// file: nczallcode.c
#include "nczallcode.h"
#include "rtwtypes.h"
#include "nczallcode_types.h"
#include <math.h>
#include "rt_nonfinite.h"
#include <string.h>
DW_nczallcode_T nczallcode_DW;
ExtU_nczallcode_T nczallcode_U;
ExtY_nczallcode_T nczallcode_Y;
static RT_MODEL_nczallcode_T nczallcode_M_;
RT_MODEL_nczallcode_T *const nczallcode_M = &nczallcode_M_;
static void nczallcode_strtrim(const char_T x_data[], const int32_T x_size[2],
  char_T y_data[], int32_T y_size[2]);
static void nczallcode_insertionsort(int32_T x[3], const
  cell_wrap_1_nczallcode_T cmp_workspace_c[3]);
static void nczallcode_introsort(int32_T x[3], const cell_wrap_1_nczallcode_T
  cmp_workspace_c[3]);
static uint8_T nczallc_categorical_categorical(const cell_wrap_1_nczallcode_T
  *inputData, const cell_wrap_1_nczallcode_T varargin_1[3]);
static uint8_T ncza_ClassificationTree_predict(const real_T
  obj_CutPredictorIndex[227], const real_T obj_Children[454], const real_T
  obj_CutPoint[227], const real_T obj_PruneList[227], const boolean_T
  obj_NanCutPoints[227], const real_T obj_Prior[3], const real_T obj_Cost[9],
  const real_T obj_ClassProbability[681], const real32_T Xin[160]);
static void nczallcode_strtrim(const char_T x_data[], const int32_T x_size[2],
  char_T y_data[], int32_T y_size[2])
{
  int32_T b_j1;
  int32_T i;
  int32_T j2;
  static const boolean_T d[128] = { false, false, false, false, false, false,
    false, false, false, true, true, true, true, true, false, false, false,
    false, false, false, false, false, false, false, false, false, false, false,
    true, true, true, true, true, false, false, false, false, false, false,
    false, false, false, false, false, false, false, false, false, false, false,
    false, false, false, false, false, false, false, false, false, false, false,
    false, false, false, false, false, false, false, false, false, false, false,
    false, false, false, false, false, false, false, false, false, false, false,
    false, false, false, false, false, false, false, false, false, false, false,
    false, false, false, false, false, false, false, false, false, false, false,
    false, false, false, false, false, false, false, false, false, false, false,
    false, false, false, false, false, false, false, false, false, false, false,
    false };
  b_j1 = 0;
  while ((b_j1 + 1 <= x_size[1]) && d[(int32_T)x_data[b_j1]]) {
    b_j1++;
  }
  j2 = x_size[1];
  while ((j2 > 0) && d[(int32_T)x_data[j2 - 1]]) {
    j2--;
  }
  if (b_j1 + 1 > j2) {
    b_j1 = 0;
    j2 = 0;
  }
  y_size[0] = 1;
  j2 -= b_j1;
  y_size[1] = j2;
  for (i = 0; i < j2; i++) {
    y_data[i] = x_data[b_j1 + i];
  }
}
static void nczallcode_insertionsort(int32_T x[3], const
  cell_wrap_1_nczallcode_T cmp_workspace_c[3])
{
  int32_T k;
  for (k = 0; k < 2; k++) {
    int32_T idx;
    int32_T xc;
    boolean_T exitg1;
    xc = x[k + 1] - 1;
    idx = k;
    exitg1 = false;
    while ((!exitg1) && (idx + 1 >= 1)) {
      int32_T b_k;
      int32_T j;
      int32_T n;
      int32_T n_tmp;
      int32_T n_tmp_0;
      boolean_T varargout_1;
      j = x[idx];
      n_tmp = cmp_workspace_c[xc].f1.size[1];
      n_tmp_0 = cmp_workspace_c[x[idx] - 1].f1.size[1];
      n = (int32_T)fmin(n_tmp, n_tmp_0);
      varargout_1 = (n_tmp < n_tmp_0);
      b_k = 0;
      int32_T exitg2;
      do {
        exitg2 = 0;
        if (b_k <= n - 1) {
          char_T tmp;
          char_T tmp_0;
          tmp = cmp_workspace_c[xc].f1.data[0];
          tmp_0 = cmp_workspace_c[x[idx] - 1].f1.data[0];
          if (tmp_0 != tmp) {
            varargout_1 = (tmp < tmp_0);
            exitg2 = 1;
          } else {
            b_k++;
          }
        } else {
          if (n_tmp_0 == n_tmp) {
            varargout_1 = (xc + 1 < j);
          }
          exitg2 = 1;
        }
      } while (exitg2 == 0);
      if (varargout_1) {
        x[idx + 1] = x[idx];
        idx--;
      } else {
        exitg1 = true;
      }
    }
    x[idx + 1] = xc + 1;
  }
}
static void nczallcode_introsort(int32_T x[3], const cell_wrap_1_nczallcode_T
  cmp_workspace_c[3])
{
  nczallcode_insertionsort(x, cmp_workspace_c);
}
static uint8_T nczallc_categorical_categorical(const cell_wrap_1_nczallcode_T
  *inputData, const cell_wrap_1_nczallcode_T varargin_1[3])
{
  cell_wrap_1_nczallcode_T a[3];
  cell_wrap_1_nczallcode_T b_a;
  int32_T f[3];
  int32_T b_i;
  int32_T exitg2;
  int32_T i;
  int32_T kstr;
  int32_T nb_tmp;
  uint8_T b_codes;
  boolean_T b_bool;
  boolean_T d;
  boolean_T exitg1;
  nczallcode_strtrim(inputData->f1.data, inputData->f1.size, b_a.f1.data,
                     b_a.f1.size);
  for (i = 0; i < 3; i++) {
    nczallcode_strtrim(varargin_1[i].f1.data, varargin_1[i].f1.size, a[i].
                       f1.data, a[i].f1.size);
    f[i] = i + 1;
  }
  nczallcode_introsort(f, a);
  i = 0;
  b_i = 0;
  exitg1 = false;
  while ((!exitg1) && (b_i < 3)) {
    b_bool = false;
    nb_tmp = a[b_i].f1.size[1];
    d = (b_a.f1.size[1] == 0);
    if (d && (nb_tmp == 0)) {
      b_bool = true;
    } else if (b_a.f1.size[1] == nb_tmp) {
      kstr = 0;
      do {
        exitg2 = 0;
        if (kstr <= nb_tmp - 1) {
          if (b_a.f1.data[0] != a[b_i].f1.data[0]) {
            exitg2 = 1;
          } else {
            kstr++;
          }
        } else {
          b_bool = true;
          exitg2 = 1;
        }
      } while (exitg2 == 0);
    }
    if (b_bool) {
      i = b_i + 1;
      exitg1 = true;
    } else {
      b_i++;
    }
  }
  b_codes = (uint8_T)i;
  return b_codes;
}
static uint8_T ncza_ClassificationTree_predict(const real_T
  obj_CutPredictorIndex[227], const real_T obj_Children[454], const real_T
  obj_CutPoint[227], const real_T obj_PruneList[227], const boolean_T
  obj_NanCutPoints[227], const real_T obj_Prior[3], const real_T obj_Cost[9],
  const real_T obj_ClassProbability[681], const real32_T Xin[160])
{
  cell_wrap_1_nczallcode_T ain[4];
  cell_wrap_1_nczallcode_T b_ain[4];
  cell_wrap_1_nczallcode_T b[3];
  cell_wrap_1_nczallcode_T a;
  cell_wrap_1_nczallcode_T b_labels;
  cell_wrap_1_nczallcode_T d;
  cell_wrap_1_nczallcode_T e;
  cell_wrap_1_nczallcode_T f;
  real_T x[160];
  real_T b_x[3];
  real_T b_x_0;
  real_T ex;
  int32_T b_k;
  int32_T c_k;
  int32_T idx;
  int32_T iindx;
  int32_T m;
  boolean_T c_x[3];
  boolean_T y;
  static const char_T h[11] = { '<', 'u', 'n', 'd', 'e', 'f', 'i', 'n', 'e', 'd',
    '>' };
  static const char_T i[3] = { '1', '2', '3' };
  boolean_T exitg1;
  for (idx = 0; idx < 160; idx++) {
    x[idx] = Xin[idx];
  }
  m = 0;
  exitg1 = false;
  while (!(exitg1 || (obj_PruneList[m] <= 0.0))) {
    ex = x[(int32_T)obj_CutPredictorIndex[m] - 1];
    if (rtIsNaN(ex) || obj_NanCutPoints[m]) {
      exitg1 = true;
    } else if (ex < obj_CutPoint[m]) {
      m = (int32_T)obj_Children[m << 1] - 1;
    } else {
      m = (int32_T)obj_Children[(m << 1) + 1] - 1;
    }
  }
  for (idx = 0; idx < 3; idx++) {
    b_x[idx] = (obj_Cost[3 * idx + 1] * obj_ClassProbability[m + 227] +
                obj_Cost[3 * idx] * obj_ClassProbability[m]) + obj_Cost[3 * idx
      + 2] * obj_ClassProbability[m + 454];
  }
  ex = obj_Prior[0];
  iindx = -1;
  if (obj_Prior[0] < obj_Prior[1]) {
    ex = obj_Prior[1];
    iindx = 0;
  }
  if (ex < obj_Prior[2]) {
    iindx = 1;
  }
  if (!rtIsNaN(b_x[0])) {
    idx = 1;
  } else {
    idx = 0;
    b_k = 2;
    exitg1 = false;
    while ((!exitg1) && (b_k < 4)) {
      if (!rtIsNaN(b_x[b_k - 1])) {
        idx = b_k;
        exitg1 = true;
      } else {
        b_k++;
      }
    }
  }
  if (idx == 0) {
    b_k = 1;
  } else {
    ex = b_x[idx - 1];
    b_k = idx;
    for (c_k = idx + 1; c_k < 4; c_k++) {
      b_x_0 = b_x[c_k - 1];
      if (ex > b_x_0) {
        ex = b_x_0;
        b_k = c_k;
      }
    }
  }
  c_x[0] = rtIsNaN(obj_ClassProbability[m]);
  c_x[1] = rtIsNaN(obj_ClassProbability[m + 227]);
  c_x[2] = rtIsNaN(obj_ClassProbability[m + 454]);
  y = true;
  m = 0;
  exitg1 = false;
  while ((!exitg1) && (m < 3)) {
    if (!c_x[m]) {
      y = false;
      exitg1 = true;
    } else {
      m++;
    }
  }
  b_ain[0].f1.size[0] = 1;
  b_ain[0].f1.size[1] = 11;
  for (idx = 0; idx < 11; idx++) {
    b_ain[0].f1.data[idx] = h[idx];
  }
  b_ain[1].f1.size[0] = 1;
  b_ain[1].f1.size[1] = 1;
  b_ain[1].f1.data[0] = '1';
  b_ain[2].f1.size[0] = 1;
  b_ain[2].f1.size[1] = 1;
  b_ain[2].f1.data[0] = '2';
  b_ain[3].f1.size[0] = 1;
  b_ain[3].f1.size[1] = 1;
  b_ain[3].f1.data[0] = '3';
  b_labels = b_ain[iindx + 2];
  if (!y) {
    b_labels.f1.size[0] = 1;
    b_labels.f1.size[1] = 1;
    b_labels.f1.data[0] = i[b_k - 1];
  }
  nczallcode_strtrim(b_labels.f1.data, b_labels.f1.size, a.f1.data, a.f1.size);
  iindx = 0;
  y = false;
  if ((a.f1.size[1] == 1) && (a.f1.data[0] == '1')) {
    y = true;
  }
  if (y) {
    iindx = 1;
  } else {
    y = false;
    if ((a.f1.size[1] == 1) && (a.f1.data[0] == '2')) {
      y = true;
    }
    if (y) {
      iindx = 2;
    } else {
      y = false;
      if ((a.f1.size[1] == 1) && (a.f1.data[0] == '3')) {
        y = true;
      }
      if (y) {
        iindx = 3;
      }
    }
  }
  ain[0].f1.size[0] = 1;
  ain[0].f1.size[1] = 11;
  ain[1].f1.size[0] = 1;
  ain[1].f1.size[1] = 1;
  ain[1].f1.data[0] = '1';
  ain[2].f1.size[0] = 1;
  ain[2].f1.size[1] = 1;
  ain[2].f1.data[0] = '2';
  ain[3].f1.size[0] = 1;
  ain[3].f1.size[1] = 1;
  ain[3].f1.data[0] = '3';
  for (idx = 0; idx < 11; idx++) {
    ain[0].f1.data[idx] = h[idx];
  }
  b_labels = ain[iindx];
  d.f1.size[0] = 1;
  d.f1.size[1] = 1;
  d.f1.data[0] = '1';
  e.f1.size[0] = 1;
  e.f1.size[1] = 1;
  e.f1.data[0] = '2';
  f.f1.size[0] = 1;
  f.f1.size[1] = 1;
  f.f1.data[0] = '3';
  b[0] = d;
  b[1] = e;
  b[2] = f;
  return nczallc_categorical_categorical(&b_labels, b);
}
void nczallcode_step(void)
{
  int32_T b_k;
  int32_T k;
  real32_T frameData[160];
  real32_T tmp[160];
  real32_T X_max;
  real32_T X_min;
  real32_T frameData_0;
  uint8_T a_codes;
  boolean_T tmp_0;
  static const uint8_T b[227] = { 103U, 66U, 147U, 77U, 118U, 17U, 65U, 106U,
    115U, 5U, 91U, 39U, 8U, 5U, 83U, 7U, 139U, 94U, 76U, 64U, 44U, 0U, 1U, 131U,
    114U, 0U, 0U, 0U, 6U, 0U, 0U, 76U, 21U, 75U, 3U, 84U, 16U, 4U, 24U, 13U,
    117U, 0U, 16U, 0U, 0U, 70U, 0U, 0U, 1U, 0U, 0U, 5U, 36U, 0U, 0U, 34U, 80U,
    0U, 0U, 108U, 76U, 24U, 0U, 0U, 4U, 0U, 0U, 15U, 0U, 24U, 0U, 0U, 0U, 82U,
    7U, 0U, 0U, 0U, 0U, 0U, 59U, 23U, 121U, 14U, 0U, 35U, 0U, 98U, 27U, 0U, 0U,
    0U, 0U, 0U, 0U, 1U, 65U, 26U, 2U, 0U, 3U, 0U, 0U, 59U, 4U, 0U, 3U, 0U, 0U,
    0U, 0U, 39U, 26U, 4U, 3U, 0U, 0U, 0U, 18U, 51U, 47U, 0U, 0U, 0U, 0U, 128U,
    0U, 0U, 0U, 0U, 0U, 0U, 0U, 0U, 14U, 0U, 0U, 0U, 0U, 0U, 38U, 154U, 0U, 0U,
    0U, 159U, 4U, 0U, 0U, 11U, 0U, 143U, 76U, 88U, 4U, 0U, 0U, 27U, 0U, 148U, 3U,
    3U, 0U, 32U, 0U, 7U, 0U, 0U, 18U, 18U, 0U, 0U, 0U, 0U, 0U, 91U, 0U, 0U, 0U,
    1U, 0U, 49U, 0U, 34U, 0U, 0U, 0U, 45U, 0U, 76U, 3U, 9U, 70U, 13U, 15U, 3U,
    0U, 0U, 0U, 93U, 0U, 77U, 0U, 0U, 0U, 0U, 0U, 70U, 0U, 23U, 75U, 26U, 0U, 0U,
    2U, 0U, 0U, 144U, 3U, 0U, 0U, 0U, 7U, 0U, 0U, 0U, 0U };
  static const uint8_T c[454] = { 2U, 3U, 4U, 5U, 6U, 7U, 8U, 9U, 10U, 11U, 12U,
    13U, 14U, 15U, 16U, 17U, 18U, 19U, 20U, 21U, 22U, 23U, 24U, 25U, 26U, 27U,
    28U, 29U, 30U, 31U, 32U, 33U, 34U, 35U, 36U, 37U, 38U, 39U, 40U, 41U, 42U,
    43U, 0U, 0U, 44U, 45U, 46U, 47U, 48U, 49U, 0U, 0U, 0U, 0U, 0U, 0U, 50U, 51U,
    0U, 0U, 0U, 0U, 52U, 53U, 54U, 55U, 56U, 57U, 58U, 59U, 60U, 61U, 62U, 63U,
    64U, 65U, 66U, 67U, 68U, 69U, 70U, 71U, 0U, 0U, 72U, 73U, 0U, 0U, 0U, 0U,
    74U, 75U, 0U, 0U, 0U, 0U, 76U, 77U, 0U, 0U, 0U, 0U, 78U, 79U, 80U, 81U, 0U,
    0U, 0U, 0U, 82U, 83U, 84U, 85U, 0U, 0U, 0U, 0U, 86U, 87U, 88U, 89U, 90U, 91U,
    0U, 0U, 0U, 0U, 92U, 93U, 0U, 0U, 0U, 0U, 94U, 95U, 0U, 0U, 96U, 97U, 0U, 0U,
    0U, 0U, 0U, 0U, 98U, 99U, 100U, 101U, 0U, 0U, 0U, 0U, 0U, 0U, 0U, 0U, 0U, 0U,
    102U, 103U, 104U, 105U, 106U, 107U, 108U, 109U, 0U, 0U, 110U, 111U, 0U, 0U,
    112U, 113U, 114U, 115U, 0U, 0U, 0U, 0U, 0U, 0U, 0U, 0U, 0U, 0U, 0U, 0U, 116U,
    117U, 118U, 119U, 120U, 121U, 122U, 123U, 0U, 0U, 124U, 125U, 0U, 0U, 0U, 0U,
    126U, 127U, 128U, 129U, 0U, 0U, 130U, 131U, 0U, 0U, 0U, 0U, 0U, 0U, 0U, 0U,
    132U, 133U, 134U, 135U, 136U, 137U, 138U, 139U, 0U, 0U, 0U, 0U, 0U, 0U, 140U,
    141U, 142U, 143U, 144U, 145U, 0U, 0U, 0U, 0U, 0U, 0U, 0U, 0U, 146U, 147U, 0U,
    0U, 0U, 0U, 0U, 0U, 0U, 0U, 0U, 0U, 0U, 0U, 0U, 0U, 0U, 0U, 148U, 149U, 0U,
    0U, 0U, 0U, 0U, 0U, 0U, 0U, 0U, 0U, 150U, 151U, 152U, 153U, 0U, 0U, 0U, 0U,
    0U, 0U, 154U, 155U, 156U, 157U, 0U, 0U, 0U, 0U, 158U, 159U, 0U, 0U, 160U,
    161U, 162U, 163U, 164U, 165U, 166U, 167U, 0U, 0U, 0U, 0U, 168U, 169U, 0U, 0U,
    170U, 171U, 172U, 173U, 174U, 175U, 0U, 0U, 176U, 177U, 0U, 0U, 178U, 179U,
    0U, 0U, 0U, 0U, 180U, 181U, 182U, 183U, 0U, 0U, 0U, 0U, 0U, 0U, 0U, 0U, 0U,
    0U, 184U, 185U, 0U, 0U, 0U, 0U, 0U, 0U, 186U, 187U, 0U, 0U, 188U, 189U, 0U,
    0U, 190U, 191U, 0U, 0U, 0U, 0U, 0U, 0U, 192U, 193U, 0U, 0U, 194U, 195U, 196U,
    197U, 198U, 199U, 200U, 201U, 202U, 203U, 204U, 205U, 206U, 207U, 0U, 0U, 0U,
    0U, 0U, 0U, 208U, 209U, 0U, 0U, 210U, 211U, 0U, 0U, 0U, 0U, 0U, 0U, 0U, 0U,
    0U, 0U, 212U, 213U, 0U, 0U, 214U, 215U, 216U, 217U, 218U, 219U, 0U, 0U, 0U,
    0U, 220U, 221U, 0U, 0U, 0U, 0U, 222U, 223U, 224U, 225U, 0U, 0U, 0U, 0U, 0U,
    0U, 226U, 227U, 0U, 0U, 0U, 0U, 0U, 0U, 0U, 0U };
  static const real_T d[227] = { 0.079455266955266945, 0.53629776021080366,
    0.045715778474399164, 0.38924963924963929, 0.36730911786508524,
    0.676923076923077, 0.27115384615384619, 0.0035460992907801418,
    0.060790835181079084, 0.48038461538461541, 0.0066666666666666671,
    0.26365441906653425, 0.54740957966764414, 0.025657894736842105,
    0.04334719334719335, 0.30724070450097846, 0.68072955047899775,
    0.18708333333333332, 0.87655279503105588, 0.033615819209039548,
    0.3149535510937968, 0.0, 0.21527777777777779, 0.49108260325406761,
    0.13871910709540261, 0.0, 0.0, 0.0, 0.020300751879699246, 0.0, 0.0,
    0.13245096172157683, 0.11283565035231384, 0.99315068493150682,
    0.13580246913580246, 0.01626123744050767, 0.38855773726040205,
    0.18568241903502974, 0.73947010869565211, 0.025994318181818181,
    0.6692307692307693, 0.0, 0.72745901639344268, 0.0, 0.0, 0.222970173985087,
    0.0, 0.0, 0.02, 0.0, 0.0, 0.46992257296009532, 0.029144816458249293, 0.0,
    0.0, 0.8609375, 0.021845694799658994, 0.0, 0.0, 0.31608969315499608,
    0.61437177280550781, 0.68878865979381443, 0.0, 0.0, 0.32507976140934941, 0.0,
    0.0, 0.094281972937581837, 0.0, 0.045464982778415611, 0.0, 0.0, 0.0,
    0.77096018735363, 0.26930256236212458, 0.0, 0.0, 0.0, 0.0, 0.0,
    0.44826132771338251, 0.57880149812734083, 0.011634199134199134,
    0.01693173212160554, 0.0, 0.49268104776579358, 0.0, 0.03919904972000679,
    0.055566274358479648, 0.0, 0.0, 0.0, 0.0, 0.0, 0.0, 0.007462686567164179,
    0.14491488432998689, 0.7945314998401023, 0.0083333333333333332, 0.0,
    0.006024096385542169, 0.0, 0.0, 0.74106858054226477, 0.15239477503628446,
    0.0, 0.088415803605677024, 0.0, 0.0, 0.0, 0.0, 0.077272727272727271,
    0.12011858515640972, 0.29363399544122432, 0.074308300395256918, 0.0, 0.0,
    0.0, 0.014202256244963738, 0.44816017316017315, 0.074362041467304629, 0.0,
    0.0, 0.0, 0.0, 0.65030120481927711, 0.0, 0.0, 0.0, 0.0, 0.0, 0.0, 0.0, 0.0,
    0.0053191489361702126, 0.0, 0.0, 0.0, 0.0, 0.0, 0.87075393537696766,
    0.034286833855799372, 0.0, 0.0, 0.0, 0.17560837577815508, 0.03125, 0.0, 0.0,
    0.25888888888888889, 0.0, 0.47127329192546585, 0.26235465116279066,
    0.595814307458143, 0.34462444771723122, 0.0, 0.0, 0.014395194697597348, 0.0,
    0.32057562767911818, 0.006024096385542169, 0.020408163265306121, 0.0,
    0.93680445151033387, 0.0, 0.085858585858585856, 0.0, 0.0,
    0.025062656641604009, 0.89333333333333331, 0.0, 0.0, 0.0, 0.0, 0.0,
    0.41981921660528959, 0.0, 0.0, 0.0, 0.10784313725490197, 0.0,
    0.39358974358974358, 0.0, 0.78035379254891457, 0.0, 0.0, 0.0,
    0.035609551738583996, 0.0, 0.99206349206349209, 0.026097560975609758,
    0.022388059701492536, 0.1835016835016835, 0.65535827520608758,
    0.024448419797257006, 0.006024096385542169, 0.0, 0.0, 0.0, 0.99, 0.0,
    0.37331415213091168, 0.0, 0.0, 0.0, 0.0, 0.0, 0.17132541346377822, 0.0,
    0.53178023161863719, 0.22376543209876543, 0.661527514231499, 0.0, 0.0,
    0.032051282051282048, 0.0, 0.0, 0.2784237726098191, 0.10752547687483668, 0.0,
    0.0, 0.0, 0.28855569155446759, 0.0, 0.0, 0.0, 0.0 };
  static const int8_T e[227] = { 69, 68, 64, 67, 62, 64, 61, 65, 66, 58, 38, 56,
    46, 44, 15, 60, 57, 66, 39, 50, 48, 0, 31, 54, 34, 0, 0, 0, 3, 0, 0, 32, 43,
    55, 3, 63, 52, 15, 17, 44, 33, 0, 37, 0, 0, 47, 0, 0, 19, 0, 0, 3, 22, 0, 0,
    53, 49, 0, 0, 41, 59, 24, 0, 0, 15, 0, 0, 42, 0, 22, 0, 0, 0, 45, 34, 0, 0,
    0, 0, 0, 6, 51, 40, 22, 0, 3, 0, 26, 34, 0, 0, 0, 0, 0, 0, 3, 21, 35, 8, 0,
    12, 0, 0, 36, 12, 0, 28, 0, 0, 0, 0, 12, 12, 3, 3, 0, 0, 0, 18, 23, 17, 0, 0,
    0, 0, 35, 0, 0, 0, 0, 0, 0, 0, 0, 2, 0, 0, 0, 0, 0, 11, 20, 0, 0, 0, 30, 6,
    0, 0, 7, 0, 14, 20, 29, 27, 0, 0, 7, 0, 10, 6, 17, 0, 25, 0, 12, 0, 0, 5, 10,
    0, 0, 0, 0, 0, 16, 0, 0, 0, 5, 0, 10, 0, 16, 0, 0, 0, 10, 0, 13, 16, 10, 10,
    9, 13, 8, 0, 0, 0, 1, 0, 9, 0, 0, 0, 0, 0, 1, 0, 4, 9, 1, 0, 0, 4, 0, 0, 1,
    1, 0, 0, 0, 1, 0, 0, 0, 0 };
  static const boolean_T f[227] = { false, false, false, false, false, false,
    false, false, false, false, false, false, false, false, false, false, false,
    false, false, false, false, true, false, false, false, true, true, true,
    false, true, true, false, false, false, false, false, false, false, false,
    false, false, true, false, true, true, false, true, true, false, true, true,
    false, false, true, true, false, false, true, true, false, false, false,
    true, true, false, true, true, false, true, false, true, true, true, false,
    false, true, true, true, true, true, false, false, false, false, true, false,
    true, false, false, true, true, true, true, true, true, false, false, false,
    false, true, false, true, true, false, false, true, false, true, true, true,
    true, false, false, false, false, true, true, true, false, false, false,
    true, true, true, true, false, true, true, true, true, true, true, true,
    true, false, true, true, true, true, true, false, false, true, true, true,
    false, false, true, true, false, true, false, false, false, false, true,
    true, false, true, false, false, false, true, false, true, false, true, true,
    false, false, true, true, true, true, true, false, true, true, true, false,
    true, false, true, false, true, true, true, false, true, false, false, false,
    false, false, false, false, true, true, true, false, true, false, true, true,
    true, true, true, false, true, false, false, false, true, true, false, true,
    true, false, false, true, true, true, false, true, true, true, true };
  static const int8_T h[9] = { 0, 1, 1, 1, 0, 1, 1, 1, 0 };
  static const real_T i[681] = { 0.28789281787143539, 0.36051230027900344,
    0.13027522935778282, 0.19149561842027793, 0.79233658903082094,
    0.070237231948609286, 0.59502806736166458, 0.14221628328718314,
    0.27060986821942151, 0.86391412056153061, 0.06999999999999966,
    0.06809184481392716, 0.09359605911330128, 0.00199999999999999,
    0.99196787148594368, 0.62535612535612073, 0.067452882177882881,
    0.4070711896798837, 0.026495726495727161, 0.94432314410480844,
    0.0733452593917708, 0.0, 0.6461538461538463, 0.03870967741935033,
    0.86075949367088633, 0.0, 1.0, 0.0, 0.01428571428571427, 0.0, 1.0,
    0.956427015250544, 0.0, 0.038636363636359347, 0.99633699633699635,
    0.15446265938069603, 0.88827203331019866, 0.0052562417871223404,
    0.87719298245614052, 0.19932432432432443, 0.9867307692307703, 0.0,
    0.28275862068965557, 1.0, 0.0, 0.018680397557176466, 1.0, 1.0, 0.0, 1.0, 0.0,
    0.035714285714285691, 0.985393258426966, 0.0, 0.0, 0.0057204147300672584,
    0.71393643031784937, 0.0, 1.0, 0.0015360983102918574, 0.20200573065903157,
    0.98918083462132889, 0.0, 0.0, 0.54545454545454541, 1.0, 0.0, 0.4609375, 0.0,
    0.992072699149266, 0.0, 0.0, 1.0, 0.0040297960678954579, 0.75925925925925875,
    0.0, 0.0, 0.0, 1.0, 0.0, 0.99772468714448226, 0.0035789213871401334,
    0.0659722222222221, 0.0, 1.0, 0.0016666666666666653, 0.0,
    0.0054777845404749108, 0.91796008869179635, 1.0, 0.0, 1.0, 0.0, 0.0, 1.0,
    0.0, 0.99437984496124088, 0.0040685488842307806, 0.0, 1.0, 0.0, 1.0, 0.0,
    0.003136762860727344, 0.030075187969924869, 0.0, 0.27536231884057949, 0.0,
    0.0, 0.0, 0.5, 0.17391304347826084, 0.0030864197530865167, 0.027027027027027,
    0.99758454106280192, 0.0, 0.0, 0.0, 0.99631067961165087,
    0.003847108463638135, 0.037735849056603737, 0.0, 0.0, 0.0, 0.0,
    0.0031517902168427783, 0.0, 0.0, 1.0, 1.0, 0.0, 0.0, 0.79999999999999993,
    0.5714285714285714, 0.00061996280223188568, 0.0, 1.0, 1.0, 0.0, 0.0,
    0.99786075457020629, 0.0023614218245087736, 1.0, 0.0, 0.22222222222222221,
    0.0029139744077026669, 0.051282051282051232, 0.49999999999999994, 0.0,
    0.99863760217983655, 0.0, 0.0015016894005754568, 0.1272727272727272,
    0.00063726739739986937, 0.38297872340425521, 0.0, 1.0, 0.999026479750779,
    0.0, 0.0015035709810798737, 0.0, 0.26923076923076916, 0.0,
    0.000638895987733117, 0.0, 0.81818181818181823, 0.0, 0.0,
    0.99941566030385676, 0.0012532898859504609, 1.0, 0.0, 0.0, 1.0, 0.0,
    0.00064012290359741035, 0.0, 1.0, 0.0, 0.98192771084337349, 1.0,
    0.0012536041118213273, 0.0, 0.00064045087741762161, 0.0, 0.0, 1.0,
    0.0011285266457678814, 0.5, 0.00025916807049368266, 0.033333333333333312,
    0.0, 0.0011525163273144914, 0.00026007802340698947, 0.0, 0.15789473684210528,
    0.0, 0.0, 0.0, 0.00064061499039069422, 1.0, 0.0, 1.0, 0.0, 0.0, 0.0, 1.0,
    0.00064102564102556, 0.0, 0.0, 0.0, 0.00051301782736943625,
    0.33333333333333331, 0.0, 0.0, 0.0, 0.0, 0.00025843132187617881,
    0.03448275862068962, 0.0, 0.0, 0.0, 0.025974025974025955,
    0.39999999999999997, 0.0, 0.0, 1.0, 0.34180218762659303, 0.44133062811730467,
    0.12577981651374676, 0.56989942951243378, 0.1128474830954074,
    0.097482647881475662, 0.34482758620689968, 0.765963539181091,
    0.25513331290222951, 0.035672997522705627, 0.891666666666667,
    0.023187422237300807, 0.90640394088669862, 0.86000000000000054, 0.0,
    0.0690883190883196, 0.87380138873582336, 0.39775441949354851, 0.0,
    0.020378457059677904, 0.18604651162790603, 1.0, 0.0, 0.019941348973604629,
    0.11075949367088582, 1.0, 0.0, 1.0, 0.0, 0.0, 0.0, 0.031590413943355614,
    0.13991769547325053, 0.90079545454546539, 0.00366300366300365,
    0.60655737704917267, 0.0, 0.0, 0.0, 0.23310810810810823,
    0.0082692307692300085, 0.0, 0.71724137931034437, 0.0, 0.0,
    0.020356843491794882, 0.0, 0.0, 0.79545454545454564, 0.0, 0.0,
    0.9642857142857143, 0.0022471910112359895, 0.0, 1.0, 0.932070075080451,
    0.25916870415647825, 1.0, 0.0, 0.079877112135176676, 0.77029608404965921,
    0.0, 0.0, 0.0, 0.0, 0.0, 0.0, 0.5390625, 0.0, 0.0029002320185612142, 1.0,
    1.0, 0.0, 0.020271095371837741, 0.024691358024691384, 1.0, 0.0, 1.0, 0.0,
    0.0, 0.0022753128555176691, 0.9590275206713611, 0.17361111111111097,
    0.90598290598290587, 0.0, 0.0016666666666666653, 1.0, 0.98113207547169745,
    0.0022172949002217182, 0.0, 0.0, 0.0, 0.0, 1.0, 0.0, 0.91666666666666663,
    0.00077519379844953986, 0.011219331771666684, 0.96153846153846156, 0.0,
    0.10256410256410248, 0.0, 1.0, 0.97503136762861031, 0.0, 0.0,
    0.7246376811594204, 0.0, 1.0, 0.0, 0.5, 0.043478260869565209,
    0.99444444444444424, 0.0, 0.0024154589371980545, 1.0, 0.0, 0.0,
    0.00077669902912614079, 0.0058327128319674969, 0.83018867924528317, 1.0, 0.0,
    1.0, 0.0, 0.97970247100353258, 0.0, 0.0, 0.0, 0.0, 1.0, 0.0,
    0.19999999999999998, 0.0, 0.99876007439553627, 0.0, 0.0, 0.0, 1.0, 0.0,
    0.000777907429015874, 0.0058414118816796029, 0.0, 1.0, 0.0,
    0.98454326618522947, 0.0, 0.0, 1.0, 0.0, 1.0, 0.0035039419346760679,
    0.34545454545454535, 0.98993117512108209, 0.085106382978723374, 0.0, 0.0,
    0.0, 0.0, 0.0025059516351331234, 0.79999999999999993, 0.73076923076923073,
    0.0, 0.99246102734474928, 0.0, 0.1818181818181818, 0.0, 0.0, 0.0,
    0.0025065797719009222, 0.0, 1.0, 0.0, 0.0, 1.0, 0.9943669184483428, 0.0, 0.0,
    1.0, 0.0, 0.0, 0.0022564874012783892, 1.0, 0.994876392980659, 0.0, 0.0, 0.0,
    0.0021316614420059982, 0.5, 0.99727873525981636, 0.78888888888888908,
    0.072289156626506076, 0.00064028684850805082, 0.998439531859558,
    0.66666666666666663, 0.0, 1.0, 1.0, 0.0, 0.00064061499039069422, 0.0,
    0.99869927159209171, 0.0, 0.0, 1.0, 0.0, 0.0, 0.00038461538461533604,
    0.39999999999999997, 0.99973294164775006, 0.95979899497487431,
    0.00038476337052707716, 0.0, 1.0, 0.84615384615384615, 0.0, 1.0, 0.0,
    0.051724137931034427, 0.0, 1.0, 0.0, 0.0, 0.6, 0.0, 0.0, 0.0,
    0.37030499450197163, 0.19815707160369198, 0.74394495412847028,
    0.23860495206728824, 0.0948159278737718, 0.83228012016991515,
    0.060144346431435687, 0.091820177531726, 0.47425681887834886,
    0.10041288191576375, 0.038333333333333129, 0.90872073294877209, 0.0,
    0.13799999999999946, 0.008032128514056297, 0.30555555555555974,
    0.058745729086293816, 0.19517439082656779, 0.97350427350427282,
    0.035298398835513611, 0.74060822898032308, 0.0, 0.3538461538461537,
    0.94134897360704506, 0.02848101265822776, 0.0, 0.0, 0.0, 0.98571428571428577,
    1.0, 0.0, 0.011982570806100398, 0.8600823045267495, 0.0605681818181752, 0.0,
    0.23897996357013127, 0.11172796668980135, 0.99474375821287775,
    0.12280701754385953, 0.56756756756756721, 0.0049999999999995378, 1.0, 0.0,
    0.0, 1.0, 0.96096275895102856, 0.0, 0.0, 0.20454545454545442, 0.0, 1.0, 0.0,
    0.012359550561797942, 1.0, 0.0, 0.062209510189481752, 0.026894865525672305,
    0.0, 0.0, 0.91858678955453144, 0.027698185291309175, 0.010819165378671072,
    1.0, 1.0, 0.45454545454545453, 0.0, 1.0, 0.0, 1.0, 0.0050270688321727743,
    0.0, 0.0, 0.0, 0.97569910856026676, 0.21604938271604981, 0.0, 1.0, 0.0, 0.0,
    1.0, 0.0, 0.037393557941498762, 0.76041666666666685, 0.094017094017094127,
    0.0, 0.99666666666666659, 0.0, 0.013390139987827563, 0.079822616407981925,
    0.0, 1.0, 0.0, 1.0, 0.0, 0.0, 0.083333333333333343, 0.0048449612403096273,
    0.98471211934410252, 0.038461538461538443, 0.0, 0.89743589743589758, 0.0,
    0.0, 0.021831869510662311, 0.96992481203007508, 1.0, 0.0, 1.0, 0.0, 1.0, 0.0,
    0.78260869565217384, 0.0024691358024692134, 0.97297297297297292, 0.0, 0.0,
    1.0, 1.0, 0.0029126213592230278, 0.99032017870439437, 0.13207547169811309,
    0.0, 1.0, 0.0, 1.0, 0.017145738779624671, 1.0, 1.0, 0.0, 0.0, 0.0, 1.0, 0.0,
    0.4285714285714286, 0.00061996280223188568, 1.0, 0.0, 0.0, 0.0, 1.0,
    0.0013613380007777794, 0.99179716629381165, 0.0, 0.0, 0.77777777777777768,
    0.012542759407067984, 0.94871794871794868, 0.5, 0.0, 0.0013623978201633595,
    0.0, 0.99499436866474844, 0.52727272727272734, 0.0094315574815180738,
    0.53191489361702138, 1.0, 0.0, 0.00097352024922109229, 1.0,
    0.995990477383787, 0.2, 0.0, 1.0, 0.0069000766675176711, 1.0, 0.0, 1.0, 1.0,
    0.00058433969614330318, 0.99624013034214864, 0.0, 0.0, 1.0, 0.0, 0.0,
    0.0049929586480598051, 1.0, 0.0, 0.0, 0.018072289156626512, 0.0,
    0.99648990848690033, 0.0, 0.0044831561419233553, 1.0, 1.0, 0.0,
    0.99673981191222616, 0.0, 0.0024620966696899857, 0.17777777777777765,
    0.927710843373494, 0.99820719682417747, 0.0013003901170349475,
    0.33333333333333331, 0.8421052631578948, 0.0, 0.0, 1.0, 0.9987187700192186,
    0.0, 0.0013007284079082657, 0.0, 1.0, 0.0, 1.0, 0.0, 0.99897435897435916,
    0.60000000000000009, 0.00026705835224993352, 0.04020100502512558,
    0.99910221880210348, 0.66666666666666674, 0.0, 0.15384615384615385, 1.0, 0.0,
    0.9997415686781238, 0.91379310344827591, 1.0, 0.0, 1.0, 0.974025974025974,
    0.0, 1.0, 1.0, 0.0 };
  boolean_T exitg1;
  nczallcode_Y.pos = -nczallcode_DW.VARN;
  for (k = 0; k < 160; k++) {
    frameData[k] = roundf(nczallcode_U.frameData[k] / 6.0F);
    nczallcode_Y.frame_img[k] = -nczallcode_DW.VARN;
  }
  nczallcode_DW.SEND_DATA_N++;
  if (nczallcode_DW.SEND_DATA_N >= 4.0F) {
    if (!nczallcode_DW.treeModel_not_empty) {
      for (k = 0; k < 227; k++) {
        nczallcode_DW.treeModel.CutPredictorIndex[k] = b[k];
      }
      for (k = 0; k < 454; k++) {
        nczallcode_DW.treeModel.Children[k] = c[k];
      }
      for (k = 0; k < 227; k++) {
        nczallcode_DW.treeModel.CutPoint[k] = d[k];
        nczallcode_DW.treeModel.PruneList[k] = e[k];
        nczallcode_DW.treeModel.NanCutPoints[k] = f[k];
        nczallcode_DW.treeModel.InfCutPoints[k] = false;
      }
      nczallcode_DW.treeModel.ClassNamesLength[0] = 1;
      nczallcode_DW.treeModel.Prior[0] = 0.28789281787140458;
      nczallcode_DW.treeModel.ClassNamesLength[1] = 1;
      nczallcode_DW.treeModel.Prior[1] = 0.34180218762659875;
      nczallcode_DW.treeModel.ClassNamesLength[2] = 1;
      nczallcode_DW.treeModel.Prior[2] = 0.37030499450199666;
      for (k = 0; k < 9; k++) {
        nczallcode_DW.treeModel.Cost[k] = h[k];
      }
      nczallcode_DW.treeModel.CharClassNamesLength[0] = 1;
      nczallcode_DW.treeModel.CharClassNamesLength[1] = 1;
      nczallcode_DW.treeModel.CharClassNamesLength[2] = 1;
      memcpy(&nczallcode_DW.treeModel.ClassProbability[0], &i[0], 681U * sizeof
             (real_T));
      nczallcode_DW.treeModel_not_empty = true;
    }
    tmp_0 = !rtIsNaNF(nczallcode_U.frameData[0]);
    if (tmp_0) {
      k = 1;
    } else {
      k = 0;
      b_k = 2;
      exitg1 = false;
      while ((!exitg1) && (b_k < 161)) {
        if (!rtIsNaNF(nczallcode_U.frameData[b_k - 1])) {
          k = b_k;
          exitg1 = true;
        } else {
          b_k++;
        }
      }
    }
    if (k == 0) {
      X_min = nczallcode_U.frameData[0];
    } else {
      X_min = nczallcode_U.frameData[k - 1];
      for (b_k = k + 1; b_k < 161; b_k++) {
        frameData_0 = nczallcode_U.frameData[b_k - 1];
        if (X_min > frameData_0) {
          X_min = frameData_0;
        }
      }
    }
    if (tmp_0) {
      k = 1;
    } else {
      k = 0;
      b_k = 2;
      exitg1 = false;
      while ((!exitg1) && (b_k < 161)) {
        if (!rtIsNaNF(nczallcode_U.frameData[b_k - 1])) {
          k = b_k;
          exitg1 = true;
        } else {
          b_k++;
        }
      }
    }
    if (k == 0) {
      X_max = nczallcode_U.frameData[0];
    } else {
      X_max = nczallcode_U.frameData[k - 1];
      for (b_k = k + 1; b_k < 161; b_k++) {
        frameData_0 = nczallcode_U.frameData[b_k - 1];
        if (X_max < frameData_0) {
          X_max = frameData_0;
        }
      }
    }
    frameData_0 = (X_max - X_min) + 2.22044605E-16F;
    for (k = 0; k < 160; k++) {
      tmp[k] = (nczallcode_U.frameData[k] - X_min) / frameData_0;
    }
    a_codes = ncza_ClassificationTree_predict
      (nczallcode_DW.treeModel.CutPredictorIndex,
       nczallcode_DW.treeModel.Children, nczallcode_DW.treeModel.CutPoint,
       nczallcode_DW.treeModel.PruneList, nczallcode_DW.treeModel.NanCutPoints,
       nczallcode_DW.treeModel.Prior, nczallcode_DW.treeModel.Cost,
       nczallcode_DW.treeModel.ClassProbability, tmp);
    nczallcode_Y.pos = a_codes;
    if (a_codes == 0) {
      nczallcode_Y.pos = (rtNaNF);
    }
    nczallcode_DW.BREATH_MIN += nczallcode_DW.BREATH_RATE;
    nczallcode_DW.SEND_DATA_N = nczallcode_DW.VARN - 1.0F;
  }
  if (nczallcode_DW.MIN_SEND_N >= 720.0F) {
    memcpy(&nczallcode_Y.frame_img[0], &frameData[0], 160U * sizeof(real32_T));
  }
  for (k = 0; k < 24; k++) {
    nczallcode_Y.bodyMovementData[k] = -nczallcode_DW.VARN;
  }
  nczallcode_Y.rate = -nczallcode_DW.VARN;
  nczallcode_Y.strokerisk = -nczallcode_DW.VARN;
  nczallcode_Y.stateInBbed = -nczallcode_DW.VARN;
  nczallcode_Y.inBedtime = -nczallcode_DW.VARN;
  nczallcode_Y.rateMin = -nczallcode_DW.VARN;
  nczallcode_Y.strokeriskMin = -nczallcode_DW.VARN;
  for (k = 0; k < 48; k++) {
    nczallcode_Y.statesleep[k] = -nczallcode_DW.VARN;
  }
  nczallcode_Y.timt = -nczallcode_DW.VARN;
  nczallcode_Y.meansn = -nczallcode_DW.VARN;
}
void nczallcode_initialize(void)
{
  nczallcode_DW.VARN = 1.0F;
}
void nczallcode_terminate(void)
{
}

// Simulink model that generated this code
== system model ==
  frameData : Inport
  Inport#1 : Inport
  bodyMovementData : Outport  <- 1: MATLABFunction#1
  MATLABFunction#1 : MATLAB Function  <- 1: frameData, 2: Inport#1
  rate : Outport  <- 1: MATLABFunction#1/2
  strokerisk : Outport  <- 1: MATLABFunction#1/3
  stateInBbed : Outport  <- 1: MATLABFunction#1/4
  inBedtime : Outport  <- 1: MATLABFunction#1/5
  rateMin : Outport  <- 1: MATLABFunction#1/6
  strokeriskMin : Outport  <- 1: MATLABFunction#1/7
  statesleep : Outport  <- 1: MATLABFunction#1/8
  timt : Outport  <- 1: MATLABFunction#1/9
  meansn : Outport  <- 1: MATLABFunction#1/10
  frame_img : Outport  <- 1: MATLABFunction#1/11
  pos : Outport  <- 1: MATLABFunction#1/12
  DataStoreMemory#1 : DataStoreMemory  DataStoreName=VARN  InitialValue=1
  DataStoreMemory#2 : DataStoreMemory  DataStoreName=G_INBED_TIM
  DataStoreMemory#3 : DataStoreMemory  DataStoreName=Awake_sleep_array  InitialValue=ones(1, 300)
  DataStoreMemory#4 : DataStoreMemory  DataStoreName=BREATH_RATE
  DataStoreMemory#5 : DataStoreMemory  DataStoreName=MIN_SEND_N
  DataStoreMemory#6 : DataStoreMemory  DataStoreName=STROKE_RISK_MIN
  DataStoreMemory#7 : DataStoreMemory  DataStoreName=BREATH_MIN
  DataStoreMemory#8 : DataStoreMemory  DataStoreName=BATCH_FRA_MEAN
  DataStoreMemory#9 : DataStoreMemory  DataStoreName=TWENTY_SEC
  DataStoreMemory#10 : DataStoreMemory  DataStoreName=STATE_SLEEP  InitialValue=[0,0,0,0,0,0,0,0,0,0,0,0,0,0,0,0,0,0,0,0,0,0,0,0,0,0,0,0,0,0,0,0,0,0,0,0,0,0,0,0,0,0,0,0,0,0,0,0]
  DataStoreMemory#11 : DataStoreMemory  DataStoreName=FRAME_DIFF  InitialValue=[0,0,0,0,0,0,0,0,0,0,0,0,0,0,0,0]
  DataStoreMemory#12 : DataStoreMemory  DataStoreName=ITER
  DataStoreMemory#13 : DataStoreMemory  DataStoreName=G_STATE_INBED
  DataStoreMemory#14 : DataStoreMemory  DataStoreName=L_R_M_FREATUE  InitialValue=[0,0,0,0,0,0,0,0,0,0,0,0,0,0,0,0,0,0,0,0,0,0,0,0,0,0,0,0,0,0,0,0,0,0,0,0,0,0,0,0,0,0,0,0,0,0,0,0,0,0,0,0,0,0,0,0,0,0,0,0,0,0,0,0,0,0,0,0,0,0,0,0,0,0,0,0,0,0,0,0,0,0,0,0,0,0,0,0,0,0,0,0,0,0,0,0,0,0,0,0,0,0,0,0,0,0,0,0,0,0,0,0,0,0,0,0,0,0,0,0,0,0,0,0,0,0,0,0,0,0,0,0,0,0,0,0,0,0,0,0,0,0,0,0,0,0,0,0,0,0,0,0,0,0,0,0,0,0,0,0,0,0,0,0,0,0,0,0,0,0,0,0,0,0,0,0,0,0,0,0]
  DataStoreMemory#15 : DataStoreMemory  DataStoreName=LEFT_RIGHT_MOVE_SUM  InitialValue=[0,0,0,0]
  DataStoreMemory#16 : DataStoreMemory  DataStoreName=Awake_sleep_average  InitialValue=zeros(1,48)
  DataStoreMemory#17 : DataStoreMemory  DataStoreName=onbednum
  DataStoreMemory#18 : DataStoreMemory  DataStoreName=R_ALARM  InitialValue=[0,0,0,0,0,0,0,0,0,0,0,0,0,0,0,0,0,0,0,0,0,0,0,0,0,0,0,0,0,0,0,0,0,0,0,0,0,0,0,0,0,0,0,0,0,0,0,0,0,0,0,0,0,0,0,0,0,0,0,0,0,0,0,0,0,0,0,0,0,0,0,0,0,0,0,0,0,0,0,0,0,0,0,0,0,0,0,0,0,0,0,0,0,0,0,0,0,0,0,0,0,0,0,0,0,0,0,0,0,0,0,0,0,0,0,0,0,0,0,0,0,0,0,0,0,0,0,0,0,0,0,0,0,0,0,0,0,0,0,0,0,0,0,0,0,0,0,0,0,0,0,0,0,0,0,0,0,0,0,0,0,0,0,0,0,0,0,0,0,0,0,0,0,0,0,0,0,0,0,0]
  DataStoreMemory#19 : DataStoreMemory  DataStoreName=BREATH_SW
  DataStoreMemory#20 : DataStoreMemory  DataStoreName=PRESSURE_MEAN
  DataStoreMemory#21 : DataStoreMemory  DataStoreName=still_or_life
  DataStoreMemory#22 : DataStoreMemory  DataStoreName=ALARM_NUM
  DataStoreMemory#23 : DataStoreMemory  DataStoreName=BODY_MOVE_NUM
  DataStoreMemory#24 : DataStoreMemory  DataStoreName=ALL_MOVE_NUM
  DataStoreMemory#25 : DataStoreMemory  DataStoreName=ONBED_SW
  DataStoreMemory#26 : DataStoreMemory  DataStoreName=inBedTimer
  DataStoreMemory#27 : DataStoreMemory  DataStoreName=BREATH_COUNT
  DataStoreMemory#28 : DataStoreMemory  DataStoreName=TRIGGER_COUNT
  DataStoreMemory#29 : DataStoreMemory  DataStoreName=PRO_FRAME  InitialValue=[0,0,0,0,0,0,0,0,0,0,0,0,0,0,0,0;0,0,0,0,0,0,0,0,0,0,0,0,0,0,0,0;0,0,0,0,0,0,0,0,0,0,0,0,0,0,0,0;0,0,0,0,0,0,0,0,0,0,0,0,0,0,0,0;0,0,0,0,0,0,0,0,0,0,0,0,0,0,0,0;0,0,0,0,0,0,0,0,0,0,0,0,0,0,0,0;0,0,0,0,0,0,0,0,0,0,0,0,0,0,0,0;0,0,0,0,0,0,0,0,0,0,0,0,0,0,0,0;0,0,0,0,0,0,0,0,0,0,0,0,0,0,0,0;0,0,0,0,0,0,0,0,0,0,0,0,0,0,0,0]
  DataStoreMemory#30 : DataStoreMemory  DataStoreName=delay_count  InitialValue=20
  DataStoreMemory#31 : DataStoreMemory  DataStoreName=previousFramesArray  InitialValue=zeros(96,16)
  DataStoreMemory#32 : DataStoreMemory  DataStoreName=BREATH_COUNTArray  InitialValue=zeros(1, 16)
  DataStoreMemory#33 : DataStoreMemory  DataStoreName=conditionTriggerHistoryArray  InitialValue=false(5,16)
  DataStoreMemory#34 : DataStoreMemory  DataStoreName=TRIGGER_COUNTArray  InitialValue=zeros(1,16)
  DataStoreMemory#35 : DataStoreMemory  DataStoreName=dominantFrequencyArray  InitialValue=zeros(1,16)
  DataStoreMemory#36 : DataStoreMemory  DataStoreName=NCZ_TIMES
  DataStoreMemory#37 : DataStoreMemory  DataStoreName=realArr  InitialValue=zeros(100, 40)
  DataStoreMemory#38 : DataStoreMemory  DataStoreName=ALL_DIFF_IMG  InitialValue=[0,0,0,0,0,0,0,0,0,0,0,0,0,0,0,0,0,0,0,0,0,0,0,0]
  DataStoreMemory#39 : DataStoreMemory  DataStoreName=SEND_DATA_N
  DataStoreMemory#40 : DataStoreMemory  DataStoreName=STROKE_RISK
== matlab function MATLABFunction#1 ==
function [bodyMovementData,rate,strokerisk,stateInBbed,inBedtime,rateMin,strokeriskMin,statesleep,timt,meansn,frame_img, pos] = nczcode(frameData, tim)
    % 定义全局变量
    global G_INBED_TIM 
%     global G_OUTBED_TIM
%     global SW_INBED
%     global SW_OUTBED
%     global INBED_TIME %Bed leaving reminder record variable
    global realArr
%     global onBedArr
    global G_STATE_INBED
    global PRO_FRAME
    global ALL_DIFF_IMG
    global SEND_DATA_N  
    global STROKE_RISK
    global BREATH_RATE  
    global MIN_SEND_N
    global STROKE_RISK_MIN
    global BREATH_MIN
    global BATCH_FRA_MEAN
    global TWENTY_SEC       
    global STATE_SLEEP
    global FRAME_DIFF
    global ITER
    global VARN
%     global ONBED_SW
    global BREATH_SW
    global PRESSURE_MEAN
    global BODY_MOVE_NUM
%     global ALL_MOVE_LIST
%     global ALL_MOVE_NUM
    global still_or_life
    global inBedTimer
%     global previousFrames
%     global BREATH_COUNT
%     global TRIGGER_COUNT
%     global conditionTriggerHistory %still state trigger
%     global dominantFrequency
    global delay_count
    %清醒入睡数组
    global Awake_sleep_array
    global Awake_sleep_average
    %onbednum 在床持续时间计数
    global onbednum
      
      div_num = 6; %160大床整除系数
      XTest = frameData';
      frameData = round(frameData/div_num);
    % 调整数据顺序并去噪
    frameData_b = frameData; % copy of original data for breath

    framedata_fall = frameData_b';
   

    %% 初始化相关变量
    inBedFlag = 14 * VARN; %0621：2000/160
%     move_prop = VARN;
    bodyMovementData = (-1) * ones(24,1) * VARN;   
    strokerisk = (-1) * VARN;  
    strokeriskMin = (-1) * VARN;   
    rate = (-1) * VARN;
    rateMin = (-1) * VARN;
    stateInBbed = (-1) * VARN;    
    statesleep = (-1) * ones(48,1) * VARN; 
    inBedtime = (-1) * VARN;
    timt = (-1) * VARN;
    meansn = (-1) * VARN;
    pos = (-1) * VARN;
    frame_img = (-1) * ones(160,1) * VARN;
%     samplingRate = 12 * VARN;
%     alarm_switch = 0;
%     on_mat_flag = 0; %在垫标志位240703
    SEND_DATA_N = SEND_DATA_N+1;

    %% 体动赋值
    gain = 1;
    if SEND_DATA_N*gain >= 4  
        pos = single(predictTree(XTest));
%         rate = BODY_MOVE_NUM;%测试
        BREATH_MIN = BREATH_MIN + BREATH_RATE;
        SEND_DATA_N = VARN - 1;
        still_or_life = VARN - 1;
    end

    %% 数据处理和传输
    if MIN_SEND_N*gain >= 720
        frame_img = reshape(frameData, 160, 1);
    end
end

%% 辅助函数

function YPred = predictTree(XTest)
    % 加载预训练的决策树模型
    persistent treeModel
    if isempty(treeModel)
        treeModel = loadCompactModel('trainedTreeModel.mat');
    end
    
    % 对输入数据进行归一化
    X_min = min(XTest, [], 2);
    X_max = max(XTest, [], 2);
    XTest_normalized = (XTest - X_min) ./ (X_max - X_min + eps);
    
    % 预测
    YPred = predict(treeModel, XTest_normalized);
end

function model = loadCompactModel(filename)
    % 加载紧凑模型
    s = coder.load(filename);
    model = s.tree;  % 将 s.treeModel 改为 s.tree
end
